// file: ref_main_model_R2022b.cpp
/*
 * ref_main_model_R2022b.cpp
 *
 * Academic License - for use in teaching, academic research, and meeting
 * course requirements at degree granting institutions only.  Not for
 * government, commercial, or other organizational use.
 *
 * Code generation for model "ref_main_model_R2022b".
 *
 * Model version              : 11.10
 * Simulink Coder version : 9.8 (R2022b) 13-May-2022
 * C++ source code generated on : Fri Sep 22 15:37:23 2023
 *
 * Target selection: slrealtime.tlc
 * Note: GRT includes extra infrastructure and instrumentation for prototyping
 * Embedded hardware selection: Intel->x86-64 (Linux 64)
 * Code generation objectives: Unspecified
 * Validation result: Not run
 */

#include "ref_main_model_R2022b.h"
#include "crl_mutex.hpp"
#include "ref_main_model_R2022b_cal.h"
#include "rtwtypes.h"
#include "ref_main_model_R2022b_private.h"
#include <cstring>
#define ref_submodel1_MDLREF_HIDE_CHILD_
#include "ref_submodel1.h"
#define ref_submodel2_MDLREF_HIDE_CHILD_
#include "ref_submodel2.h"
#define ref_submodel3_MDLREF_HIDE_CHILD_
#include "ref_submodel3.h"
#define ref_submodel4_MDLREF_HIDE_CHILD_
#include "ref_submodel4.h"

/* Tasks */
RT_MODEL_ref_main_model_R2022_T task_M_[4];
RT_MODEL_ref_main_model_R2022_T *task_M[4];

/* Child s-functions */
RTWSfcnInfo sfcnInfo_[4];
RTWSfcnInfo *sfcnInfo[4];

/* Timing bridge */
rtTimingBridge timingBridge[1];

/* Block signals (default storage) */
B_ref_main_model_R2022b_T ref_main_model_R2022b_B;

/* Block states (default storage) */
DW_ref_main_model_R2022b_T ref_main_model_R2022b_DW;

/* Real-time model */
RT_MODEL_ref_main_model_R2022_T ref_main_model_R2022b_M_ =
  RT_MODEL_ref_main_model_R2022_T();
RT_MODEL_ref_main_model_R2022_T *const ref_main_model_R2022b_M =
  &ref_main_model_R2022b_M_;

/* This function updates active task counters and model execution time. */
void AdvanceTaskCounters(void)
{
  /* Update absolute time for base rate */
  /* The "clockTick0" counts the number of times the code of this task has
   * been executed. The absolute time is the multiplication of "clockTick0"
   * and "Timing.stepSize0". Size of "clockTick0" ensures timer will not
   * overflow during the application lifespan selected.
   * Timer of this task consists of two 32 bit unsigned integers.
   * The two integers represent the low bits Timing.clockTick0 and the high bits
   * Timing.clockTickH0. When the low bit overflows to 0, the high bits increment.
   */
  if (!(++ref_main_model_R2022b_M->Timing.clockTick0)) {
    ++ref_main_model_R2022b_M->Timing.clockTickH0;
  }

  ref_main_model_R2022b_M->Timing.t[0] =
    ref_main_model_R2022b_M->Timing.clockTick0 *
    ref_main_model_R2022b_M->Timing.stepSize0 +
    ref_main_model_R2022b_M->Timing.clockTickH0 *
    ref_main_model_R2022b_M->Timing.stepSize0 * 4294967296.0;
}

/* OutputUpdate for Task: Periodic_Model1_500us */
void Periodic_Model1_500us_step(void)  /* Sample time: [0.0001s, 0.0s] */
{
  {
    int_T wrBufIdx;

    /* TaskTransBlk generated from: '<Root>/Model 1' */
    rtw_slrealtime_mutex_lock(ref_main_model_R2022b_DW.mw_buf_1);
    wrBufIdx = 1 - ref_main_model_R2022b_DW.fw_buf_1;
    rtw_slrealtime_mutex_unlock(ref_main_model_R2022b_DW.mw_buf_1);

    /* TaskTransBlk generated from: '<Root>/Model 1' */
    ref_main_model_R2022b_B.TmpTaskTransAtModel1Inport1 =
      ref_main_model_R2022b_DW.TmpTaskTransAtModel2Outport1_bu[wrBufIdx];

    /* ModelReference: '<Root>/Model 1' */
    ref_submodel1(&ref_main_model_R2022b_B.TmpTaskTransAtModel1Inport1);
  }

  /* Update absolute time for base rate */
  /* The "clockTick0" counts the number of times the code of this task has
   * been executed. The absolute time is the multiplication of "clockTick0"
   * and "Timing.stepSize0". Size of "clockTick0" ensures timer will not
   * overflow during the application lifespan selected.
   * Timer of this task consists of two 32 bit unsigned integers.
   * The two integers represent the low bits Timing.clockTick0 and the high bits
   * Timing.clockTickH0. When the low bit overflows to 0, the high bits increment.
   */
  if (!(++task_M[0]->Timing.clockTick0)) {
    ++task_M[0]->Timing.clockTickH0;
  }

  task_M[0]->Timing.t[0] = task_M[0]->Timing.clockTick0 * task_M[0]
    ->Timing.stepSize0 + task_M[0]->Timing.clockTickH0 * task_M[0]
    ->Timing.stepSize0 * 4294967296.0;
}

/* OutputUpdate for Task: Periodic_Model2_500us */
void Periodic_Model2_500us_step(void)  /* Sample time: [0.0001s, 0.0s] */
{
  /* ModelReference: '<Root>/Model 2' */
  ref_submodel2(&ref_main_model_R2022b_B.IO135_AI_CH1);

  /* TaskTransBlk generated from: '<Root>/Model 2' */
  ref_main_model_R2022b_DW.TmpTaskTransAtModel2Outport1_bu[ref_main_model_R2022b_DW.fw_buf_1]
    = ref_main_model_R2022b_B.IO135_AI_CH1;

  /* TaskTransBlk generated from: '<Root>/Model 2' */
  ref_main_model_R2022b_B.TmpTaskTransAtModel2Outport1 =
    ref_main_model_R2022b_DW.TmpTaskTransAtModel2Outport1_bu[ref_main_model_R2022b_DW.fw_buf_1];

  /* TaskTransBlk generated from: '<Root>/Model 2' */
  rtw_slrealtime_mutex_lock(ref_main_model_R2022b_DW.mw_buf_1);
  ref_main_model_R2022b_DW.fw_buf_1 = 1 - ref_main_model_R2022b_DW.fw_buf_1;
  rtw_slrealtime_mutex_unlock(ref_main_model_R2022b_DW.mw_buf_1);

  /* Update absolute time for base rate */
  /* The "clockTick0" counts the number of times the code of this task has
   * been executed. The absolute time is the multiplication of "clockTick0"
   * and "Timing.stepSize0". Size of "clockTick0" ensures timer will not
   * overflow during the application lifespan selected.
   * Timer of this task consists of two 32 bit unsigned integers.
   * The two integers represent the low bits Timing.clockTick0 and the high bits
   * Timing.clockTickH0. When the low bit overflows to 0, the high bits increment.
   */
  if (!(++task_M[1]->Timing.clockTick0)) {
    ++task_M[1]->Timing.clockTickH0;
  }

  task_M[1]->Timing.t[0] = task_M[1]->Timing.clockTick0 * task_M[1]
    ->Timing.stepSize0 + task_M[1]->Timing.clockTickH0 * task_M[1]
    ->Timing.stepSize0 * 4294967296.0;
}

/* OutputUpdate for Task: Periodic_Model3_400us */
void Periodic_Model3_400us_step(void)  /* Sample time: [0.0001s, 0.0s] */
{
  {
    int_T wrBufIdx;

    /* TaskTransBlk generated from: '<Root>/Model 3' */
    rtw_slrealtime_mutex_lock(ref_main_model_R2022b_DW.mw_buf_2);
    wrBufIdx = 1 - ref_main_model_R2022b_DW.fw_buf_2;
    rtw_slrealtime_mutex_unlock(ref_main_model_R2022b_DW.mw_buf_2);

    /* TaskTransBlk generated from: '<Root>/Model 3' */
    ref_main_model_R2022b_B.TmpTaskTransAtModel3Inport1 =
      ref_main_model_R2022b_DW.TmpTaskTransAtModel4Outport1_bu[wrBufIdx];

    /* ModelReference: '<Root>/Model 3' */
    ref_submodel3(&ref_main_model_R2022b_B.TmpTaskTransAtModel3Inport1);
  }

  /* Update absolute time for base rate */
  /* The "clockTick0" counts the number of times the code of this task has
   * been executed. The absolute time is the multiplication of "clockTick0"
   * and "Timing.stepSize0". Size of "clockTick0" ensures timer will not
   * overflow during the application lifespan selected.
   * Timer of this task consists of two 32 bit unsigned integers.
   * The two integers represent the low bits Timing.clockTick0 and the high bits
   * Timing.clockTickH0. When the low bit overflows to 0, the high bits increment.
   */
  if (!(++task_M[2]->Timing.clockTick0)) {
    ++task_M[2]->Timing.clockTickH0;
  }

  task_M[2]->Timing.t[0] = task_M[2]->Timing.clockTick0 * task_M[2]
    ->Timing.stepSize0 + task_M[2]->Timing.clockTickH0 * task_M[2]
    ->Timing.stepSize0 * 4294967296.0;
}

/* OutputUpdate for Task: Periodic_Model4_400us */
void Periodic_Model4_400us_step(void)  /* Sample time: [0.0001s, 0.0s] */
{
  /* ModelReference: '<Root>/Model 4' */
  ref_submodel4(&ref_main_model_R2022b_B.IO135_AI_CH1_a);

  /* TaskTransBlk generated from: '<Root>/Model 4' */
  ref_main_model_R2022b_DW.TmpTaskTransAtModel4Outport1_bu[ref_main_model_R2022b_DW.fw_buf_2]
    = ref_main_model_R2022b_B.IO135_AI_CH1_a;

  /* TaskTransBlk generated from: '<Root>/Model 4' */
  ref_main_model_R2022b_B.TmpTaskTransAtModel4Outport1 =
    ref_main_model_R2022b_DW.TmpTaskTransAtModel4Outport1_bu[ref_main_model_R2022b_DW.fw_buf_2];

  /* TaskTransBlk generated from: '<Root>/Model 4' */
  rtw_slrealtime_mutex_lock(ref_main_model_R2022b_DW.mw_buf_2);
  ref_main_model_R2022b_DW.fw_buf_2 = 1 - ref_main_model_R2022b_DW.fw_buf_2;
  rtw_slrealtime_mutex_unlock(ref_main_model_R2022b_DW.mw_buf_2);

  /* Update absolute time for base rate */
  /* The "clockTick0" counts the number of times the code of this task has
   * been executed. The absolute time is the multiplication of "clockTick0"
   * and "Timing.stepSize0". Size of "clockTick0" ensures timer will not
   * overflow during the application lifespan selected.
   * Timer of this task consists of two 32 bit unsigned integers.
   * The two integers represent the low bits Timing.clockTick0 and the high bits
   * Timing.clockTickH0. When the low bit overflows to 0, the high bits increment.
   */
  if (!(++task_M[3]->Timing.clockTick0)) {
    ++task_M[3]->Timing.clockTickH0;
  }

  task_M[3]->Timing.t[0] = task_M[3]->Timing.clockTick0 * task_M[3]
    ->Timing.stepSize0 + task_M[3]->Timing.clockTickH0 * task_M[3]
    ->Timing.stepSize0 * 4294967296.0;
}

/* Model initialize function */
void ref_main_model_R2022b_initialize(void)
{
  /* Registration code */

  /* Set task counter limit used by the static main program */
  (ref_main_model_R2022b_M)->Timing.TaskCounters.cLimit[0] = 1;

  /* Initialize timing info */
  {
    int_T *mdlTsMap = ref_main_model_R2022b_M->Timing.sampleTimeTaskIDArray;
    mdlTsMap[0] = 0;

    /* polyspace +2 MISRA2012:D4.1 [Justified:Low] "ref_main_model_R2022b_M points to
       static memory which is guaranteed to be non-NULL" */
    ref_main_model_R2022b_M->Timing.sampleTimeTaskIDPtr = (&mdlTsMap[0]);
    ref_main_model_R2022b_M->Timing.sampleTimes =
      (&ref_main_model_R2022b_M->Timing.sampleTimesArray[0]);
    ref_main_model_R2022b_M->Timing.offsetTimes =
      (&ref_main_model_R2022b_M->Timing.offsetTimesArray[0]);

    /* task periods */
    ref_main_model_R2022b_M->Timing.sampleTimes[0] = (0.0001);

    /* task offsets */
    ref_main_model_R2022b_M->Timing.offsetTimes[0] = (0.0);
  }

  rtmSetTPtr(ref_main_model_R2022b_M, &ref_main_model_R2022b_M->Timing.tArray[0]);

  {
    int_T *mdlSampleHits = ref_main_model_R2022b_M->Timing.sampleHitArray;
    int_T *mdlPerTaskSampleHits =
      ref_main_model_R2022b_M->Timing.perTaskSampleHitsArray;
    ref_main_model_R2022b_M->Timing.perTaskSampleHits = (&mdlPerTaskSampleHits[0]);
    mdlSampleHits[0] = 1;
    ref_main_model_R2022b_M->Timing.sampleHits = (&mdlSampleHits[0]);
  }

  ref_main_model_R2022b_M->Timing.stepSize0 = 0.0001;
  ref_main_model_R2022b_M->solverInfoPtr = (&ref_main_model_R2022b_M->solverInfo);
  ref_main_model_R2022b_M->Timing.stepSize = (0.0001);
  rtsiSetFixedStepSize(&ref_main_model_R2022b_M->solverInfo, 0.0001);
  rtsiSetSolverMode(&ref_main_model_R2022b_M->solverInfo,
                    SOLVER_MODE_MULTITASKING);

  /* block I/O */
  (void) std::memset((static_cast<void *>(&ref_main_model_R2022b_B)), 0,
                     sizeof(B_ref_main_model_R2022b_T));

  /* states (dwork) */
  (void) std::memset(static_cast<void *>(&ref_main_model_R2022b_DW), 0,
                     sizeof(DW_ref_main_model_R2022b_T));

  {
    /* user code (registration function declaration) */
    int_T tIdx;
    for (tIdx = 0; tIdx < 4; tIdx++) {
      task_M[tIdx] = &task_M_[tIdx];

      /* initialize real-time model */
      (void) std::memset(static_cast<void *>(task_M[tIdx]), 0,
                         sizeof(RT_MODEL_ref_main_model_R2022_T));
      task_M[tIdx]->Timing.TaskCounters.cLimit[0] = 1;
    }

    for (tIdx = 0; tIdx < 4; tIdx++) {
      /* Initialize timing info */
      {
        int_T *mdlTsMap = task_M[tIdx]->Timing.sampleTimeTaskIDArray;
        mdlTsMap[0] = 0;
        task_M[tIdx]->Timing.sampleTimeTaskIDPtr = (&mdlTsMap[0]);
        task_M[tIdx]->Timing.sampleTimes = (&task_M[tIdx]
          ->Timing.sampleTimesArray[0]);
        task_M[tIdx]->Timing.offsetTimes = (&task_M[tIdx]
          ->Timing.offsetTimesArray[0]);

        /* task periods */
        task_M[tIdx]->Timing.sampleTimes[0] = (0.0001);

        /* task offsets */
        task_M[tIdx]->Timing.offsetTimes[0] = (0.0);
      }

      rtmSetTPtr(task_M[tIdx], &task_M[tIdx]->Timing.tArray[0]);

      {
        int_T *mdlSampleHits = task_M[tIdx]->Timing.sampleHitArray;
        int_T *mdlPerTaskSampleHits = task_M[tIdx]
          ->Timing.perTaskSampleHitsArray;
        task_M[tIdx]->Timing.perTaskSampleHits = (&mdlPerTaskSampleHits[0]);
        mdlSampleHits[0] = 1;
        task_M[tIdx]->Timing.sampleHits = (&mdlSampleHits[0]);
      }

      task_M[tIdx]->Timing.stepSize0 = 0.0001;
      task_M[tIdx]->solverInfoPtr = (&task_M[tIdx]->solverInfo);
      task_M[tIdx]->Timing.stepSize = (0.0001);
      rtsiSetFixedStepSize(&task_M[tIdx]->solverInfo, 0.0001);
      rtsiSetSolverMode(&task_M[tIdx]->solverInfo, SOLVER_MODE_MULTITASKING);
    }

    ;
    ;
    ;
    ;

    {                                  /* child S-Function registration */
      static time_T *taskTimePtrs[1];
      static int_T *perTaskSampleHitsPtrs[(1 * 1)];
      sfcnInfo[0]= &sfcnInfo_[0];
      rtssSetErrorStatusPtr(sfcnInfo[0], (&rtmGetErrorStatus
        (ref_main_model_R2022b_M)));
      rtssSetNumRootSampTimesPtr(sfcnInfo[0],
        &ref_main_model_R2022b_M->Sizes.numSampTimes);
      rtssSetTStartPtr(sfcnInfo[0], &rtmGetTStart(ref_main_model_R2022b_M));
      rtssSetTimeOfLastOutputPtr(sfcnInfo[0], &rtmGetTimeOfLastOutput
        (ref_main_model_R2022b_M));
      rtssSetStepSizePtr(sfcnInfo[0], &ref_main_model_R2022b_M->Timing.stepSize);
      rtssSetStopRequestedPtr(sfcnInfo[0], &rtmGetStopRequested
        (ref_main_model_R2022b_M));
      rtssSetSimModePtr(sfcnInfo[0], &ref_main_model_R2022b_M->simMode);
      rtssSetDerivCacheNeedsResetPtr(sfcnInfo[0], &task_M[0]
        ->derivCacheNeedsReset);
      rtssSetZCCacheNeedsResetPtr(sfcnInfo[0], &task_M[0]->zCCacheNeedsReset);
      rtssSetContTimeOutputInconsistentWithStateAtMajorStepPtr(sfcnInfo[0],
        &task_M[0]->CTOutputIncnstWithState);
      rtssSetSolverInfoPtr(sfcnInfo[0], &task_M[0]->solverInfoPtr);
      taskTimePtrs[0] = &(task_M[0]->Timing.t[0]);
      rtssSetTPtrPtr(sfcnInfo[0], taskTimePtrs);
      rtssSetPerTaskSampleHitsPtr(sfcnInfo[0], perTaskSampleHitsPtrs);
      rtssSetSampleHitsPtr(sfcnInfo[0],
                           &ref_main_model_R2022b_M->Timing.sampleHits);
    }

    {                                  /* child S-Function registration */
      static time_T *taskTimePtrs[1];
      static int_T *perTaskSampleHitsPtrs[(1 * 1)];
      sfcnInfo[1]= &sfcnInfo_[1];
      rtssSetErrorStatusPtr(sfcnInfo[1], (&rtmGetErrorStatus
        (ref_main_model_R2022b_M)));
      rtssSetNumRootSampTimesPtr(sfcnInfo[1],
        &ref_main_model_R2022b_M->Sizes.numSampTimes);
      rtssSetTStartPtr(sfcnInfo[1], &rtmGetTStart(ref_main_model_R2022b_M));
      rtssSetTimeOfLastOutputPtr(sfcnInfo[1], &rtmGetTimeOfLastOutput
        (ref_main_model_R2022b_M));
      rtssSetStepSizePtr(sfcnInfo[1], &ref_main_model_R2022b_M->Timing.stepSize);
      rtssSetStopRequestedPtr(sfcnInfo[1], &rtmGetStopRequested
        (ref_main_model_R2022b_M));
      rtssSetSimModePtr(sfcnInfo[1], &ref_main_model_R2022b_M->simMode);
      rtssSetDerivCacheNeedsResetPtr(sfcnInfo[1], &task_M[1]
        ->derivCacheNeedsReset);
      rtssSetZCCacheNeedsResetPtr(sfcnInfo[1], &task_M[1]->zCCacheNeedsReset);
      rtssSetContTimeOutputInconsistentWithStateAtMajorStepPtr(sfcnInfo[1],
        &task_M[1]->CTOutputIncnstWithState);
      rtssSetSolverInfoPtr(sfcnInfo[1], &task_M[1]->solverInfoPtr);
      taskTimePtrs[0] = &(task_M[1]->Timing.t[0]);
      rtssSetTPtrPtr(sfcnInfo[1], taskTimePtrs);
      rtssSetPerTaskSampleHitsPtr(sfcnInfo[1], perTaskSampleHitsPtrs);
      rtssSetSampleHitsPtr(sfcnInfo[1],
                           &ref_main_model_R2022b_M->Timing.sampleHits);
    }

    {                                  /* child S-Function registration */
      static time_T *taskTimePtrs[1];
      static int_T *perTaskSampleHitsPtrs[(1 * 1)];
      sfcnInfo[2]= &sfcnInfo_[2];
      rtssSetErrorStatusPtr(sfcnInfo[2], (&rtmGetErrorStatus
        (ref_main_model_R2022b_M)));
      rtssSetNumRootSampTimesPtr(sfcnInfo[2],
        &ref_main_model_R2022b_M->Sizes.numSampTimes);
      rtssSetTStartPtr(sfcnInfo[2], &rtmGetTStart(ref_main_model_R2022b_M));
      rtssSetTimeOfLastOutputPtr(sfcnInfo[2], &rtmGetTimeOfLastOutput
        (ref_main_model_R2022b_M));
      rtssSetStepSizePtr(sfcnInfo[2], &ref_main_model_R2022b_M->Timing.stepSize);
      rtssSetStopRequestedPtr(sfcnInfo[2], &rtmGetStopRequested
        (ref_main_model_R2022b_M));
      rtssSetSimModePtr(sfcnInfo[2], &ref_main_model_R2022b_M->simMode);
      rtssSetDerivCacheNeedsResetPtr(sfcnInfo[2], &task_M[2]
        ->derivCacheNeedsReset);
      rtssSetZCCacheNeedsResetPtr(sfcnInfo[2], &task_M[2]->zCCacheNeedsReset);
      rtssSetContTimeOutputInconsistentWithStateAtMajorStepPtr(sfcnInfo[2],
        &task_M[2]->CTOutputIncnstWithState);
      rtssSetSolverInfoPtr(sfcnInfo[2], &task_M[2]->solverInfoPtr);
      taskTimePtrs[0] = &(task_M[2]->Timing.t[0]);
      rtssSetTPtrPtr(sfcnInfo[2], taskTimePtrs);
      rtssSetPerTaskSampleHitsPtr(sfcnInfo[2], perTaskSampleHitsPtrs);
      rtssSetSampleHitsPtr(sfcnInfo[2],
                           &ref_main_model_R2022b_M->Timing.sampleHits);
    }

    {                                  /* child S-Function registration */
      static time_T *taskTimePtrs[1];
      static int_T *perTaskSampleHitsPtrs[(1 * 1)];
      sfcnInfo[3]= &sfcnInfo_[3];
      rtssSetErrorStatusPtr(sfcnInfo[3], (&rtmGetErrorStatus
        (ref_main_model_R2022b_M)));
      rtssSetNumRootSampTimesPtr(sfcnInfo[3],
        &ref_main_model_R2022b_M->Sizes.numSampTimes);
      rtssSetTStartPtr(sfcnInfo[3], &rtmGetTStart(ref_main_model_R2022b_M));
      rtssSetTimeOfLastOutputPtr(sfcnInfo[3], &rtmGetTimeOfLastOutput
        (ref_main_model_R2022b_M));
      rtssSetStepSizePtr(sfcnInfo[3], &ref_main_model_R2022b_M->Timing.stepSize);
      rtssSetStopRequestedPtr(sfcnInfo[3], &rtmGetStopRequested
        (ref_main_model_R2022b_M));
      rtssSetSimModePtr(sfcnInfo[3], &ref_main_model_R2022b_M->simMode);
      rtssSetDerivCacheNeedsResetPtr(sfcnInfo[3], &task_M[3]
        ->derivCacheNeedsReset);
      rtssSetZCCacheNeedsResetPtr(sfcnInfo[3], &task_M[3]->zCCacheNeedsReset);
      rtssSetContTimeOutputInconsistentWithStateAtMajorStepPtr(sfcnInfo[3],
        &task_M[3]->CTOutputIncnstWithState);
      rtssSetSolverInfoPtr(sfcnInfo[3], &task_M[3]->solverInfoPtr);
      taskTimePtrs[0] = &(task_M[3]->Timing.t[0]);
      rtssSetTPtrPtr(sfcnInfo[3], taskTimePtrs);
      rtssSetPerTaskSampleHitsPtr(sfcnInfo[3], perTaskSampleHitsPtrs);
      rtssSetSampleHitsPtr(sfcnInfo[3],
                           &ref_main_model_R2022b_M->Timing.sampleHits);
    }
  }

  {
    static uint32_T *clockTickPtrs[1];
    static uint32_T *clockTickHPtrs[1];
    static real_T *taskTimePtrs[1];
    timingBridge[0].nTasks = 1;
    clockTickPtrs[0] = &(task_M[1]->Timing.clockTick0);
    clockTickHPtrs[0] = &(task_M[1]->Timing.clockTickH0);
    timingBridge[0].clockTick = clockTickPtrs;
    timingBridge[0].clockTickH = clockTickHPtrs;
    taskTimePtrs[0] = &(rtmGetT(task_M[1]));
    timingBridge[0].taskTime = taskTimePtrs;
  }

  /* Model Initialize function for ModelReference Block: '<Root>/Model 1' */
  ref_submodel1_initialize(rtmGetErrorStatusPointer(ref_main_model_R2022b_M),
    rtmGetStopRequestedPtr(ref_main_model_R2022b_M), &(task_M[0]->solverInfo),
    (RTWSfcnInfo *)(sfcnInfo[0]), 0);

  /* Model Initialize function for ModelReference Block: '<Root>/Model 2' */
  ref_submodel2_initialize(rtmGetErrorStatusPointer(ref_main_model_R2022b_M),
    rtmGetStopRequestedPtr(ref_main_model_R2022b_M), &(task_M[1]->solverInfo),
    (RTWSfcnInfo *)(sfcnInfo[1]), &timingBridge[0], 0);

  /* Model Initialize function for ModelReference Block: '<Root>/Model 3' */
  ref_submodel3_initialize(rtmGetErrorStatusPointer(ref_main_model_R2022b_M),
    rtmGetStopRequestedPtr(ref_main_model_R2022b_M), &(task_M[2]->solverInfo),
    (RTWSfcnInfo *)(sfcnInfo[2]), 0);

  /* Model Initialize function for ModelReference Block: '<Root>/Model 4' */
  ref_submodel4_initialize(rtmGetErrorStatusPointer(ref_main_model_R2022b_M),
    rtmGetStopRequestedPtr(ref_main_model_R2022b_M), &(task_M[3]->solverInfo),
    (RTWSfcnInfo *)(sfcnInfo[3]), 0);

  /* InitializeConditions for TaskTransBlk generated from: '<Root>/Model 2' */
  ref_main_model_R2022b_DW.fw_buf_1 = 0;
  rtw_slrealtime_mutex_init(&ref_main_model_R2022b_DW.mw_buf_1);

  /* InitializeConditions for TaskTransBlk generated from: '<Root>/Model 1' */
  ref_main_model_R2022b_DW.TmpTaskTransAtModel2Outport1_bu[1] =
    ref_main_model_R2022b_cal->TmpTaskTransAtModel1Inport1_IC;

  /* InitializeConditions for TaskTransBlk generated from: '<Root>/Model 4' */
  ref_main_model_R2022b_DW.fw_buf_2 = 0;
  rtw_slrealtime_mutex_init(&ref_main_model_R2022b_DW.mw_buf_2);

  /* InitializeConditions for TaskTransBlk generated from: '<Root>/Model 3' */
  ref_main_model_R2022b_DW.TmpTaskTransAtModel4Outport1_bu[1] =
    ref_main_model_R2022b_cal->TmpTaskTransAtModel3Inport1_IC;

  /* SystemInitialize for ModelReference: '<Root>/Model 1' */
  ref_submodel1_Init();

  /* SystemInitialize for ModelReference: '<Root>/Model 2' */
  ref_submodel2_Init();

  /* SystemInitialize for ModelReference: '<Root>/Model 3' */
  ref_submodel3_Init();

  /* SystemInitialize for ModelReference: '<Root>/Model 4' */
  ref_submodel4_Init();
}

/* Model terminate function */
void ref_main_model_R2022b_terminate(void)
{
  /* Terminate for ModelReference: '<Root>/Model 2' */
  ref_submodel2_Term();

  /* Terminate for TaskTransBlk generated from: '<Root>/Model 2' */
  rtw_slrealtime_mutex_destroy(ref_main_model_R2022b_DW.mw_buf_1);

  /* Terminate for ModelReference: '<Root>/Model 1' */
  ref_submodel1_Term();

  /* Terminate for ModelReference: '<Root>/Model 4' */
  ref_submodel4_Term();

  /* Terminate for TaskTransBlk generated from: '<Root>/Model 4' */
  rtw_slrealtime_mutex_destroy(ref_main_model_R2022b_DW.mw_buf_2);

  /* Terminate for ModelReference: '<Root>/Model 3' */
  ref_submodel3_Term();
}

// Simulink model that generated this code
simulink model "ref_main_model_R2022b"  (R2022b)
settings: Solver=FixedStepDiscrete  StartTime=0.0  StopTime=inf  RelTol=1e-3  EnableMultiTasking=on

== system ref_main_model_R2022b ==
  Model 1 : ModelReference  ModelNameDialog=ref_submodel1.slx  SimulationMode=Normal  ModelReferenceVersion=11.4
  Model 2 : ModelReference  ModelNameDialog=ref_submodel2.slx  SimulationMode=Normal  ModelReferenceVersion=11.12
  Model 3 : ModelReference  ModelNameDialog=ref_submodel3.slx  SimulationMode=Normal  ModelReferenceVersion=11.7
  Model 4 : ModelReference  ModelNameDialog=ref_submodel4.slx  SimulationMode=Normal  ModelReferenceVersion=11.8
  wires:
  Model 2/1 -> Model 1/1
  Model 4/1 -> Model 3/1
